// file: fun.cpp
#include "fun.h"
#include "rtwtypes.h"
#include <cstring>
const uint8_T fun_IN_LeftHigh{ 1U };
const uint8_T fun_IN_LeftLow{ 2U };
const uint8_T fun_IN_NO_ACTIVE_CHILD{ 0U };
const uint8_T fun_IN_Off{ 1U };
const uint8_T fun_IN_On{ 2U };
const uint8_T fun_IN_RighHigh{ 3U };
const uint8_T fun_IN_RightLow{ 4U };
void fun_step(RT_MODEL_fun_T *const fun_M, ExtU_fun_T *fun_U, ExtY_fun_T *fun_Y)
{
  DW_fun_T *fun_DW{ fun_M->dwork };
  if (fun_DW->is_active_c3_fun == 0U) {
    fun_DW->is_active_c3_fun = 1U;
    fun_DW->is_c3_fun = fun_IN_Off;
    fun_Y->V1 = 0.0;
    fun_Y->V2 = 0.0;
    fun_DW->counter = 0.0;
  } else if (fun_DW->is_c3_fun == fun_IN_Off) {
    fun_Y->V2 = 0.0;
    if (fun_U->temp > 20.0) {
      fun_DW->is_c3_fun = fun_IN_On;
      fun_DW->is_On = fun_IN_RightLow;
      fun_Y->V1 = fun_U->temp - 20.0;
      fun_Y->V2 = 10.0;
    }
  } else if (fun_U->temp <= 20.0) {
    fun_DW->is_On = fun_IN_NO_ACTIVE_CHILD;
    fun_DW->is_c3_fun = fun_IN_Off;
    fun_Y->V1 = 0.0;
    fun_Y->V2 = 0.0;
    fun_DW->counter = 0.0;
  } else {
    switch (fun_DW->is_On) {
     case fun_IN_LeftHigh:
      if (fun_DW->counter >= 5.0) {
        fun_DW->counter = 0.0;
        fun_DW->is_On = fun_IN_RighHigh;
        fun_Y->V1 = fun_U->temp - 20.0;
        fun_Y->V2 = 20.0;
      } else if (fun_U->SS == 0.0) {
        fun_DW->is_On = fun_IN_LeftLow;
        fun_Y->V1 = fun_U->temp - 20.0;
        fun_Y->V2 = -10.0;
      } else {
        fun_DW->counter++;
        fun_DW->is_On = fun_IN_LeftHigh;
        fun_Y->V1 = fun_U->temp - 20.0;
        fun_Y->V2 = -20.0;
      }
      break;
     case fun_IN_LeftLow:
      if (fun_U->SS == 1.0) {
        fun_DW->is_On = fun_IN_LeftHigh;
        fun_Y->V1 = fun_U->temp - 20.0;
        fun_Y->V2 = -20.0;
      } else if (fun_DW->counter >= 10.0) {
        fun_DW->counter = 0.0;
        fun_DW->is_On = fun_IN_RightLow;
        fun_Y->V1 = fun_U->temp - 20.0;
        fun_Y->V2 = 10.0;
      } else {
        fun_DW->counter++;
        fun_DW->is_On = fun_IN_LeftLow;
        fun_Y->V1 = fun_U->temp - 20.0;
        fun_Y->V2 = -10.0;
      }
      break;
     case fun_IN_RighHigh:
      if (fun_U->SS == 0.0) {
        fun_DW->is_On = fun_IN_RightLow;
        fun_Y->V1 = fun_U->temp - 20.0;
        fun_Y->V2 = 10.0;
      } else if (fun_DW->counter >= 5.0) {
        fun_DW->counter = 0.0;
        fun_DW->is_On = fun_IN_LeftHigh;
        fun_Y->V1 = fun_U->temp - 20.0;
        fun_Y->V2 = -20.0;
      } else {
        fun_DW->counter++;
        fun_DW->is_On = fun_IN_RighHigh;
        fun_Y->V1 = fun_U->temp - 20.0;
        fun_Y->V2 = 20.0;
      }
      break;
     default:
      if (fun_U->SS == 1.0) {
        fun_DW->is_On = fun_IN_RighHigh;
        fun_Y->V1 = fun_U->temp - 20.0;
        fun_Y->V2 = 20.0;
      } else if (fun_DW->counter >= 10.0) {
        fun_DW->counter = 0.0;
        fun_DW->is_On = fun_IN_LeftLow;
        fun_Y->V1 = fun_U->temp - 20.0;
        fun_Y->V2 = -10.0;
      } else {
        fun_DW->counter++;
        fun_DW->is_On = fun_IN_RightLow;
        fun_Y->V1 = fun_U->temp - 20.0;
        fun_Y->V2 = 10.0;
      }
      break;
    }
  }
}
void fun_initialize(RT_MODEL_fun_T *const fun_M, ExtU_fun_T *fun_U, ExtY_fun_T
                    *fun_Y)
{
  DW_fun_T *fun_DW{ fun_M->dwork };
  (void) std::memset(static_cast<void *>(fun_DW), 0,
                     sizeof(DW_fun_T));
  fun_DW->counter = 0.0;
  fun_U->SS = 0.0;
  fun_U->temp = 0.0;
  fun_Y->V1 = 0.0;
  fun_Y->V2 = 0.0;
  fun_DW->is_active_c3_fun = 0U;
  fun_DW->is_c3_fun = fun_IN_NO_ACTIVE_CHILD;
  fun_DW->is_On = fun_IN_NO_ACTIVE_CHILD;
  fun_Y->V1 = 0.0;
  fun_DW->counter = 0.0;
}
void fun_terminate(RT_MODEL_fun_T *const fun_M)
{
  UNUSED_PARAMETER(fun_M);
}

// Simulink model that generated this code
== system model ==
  SS : Inport
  temp : Inport
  V1 : Outport  <- 1: Stateflowchart#1
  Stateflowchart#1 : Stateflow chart  <- 1: SS, 2: temp
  V2 : Outport  <- 1: Stateflowchart#1/2
== stateflow chart Stateflowchart#1 ==
  state On
    state RightLow
      entry:
      V1  = temp - 20;
      V2 = 10;
    state RighHigh
      entry:
      V1  = temp - 20;
      V2 = 20;
    state LeftLow
      entry:
      V1  = temp - 20;
      V2 = -10;
    state LeftHigh
      entry:
      V1  = temp - 20;
      V2 = -20;
    (default) -> RightLow
    RighHigh -> RighHigh [order 3] : {counter = counter + 1}
    RightLow -> RighHigh [order 1] : [SS == 1]
    RightLow -> RightLow [order 3] : {counter = counter +1}
    RighHigh -> RightLow [order 1] : [SS == 0]
    RightLow -> LeftLow [order 2] : [counter >= 10]{counter = 0}
    LeftLow -> RightLow [order 2] : [counter >= 10]{counter = 0}
    LeftHigh -> RighHigh [order 1] : [counter >= 5]{counter = 0}
    RighHigh -> LeftHigh [order 2] : [counter >= 5]{counter = 0}
    LeftLow -> LeftHigh [order 1] : [SS == 1]
    LeftLow -> LeftLow [order 3] : {counter = counter + 1}
    LeftHigh -> LeftHigh [order 3] : {counter = counter +1}
    LeftHigh -> LeftLow [order 2] : [SS == 0]
  state Off
    entry:
    V1 = 0;
    V2 = 0;
    counter = 0;
  (default) -> Off
  Off -> On : [temp > 20]
  On -> Off : [temp <= 20]
  data: V1 output; V2 output; SS input; counter local; temp input
